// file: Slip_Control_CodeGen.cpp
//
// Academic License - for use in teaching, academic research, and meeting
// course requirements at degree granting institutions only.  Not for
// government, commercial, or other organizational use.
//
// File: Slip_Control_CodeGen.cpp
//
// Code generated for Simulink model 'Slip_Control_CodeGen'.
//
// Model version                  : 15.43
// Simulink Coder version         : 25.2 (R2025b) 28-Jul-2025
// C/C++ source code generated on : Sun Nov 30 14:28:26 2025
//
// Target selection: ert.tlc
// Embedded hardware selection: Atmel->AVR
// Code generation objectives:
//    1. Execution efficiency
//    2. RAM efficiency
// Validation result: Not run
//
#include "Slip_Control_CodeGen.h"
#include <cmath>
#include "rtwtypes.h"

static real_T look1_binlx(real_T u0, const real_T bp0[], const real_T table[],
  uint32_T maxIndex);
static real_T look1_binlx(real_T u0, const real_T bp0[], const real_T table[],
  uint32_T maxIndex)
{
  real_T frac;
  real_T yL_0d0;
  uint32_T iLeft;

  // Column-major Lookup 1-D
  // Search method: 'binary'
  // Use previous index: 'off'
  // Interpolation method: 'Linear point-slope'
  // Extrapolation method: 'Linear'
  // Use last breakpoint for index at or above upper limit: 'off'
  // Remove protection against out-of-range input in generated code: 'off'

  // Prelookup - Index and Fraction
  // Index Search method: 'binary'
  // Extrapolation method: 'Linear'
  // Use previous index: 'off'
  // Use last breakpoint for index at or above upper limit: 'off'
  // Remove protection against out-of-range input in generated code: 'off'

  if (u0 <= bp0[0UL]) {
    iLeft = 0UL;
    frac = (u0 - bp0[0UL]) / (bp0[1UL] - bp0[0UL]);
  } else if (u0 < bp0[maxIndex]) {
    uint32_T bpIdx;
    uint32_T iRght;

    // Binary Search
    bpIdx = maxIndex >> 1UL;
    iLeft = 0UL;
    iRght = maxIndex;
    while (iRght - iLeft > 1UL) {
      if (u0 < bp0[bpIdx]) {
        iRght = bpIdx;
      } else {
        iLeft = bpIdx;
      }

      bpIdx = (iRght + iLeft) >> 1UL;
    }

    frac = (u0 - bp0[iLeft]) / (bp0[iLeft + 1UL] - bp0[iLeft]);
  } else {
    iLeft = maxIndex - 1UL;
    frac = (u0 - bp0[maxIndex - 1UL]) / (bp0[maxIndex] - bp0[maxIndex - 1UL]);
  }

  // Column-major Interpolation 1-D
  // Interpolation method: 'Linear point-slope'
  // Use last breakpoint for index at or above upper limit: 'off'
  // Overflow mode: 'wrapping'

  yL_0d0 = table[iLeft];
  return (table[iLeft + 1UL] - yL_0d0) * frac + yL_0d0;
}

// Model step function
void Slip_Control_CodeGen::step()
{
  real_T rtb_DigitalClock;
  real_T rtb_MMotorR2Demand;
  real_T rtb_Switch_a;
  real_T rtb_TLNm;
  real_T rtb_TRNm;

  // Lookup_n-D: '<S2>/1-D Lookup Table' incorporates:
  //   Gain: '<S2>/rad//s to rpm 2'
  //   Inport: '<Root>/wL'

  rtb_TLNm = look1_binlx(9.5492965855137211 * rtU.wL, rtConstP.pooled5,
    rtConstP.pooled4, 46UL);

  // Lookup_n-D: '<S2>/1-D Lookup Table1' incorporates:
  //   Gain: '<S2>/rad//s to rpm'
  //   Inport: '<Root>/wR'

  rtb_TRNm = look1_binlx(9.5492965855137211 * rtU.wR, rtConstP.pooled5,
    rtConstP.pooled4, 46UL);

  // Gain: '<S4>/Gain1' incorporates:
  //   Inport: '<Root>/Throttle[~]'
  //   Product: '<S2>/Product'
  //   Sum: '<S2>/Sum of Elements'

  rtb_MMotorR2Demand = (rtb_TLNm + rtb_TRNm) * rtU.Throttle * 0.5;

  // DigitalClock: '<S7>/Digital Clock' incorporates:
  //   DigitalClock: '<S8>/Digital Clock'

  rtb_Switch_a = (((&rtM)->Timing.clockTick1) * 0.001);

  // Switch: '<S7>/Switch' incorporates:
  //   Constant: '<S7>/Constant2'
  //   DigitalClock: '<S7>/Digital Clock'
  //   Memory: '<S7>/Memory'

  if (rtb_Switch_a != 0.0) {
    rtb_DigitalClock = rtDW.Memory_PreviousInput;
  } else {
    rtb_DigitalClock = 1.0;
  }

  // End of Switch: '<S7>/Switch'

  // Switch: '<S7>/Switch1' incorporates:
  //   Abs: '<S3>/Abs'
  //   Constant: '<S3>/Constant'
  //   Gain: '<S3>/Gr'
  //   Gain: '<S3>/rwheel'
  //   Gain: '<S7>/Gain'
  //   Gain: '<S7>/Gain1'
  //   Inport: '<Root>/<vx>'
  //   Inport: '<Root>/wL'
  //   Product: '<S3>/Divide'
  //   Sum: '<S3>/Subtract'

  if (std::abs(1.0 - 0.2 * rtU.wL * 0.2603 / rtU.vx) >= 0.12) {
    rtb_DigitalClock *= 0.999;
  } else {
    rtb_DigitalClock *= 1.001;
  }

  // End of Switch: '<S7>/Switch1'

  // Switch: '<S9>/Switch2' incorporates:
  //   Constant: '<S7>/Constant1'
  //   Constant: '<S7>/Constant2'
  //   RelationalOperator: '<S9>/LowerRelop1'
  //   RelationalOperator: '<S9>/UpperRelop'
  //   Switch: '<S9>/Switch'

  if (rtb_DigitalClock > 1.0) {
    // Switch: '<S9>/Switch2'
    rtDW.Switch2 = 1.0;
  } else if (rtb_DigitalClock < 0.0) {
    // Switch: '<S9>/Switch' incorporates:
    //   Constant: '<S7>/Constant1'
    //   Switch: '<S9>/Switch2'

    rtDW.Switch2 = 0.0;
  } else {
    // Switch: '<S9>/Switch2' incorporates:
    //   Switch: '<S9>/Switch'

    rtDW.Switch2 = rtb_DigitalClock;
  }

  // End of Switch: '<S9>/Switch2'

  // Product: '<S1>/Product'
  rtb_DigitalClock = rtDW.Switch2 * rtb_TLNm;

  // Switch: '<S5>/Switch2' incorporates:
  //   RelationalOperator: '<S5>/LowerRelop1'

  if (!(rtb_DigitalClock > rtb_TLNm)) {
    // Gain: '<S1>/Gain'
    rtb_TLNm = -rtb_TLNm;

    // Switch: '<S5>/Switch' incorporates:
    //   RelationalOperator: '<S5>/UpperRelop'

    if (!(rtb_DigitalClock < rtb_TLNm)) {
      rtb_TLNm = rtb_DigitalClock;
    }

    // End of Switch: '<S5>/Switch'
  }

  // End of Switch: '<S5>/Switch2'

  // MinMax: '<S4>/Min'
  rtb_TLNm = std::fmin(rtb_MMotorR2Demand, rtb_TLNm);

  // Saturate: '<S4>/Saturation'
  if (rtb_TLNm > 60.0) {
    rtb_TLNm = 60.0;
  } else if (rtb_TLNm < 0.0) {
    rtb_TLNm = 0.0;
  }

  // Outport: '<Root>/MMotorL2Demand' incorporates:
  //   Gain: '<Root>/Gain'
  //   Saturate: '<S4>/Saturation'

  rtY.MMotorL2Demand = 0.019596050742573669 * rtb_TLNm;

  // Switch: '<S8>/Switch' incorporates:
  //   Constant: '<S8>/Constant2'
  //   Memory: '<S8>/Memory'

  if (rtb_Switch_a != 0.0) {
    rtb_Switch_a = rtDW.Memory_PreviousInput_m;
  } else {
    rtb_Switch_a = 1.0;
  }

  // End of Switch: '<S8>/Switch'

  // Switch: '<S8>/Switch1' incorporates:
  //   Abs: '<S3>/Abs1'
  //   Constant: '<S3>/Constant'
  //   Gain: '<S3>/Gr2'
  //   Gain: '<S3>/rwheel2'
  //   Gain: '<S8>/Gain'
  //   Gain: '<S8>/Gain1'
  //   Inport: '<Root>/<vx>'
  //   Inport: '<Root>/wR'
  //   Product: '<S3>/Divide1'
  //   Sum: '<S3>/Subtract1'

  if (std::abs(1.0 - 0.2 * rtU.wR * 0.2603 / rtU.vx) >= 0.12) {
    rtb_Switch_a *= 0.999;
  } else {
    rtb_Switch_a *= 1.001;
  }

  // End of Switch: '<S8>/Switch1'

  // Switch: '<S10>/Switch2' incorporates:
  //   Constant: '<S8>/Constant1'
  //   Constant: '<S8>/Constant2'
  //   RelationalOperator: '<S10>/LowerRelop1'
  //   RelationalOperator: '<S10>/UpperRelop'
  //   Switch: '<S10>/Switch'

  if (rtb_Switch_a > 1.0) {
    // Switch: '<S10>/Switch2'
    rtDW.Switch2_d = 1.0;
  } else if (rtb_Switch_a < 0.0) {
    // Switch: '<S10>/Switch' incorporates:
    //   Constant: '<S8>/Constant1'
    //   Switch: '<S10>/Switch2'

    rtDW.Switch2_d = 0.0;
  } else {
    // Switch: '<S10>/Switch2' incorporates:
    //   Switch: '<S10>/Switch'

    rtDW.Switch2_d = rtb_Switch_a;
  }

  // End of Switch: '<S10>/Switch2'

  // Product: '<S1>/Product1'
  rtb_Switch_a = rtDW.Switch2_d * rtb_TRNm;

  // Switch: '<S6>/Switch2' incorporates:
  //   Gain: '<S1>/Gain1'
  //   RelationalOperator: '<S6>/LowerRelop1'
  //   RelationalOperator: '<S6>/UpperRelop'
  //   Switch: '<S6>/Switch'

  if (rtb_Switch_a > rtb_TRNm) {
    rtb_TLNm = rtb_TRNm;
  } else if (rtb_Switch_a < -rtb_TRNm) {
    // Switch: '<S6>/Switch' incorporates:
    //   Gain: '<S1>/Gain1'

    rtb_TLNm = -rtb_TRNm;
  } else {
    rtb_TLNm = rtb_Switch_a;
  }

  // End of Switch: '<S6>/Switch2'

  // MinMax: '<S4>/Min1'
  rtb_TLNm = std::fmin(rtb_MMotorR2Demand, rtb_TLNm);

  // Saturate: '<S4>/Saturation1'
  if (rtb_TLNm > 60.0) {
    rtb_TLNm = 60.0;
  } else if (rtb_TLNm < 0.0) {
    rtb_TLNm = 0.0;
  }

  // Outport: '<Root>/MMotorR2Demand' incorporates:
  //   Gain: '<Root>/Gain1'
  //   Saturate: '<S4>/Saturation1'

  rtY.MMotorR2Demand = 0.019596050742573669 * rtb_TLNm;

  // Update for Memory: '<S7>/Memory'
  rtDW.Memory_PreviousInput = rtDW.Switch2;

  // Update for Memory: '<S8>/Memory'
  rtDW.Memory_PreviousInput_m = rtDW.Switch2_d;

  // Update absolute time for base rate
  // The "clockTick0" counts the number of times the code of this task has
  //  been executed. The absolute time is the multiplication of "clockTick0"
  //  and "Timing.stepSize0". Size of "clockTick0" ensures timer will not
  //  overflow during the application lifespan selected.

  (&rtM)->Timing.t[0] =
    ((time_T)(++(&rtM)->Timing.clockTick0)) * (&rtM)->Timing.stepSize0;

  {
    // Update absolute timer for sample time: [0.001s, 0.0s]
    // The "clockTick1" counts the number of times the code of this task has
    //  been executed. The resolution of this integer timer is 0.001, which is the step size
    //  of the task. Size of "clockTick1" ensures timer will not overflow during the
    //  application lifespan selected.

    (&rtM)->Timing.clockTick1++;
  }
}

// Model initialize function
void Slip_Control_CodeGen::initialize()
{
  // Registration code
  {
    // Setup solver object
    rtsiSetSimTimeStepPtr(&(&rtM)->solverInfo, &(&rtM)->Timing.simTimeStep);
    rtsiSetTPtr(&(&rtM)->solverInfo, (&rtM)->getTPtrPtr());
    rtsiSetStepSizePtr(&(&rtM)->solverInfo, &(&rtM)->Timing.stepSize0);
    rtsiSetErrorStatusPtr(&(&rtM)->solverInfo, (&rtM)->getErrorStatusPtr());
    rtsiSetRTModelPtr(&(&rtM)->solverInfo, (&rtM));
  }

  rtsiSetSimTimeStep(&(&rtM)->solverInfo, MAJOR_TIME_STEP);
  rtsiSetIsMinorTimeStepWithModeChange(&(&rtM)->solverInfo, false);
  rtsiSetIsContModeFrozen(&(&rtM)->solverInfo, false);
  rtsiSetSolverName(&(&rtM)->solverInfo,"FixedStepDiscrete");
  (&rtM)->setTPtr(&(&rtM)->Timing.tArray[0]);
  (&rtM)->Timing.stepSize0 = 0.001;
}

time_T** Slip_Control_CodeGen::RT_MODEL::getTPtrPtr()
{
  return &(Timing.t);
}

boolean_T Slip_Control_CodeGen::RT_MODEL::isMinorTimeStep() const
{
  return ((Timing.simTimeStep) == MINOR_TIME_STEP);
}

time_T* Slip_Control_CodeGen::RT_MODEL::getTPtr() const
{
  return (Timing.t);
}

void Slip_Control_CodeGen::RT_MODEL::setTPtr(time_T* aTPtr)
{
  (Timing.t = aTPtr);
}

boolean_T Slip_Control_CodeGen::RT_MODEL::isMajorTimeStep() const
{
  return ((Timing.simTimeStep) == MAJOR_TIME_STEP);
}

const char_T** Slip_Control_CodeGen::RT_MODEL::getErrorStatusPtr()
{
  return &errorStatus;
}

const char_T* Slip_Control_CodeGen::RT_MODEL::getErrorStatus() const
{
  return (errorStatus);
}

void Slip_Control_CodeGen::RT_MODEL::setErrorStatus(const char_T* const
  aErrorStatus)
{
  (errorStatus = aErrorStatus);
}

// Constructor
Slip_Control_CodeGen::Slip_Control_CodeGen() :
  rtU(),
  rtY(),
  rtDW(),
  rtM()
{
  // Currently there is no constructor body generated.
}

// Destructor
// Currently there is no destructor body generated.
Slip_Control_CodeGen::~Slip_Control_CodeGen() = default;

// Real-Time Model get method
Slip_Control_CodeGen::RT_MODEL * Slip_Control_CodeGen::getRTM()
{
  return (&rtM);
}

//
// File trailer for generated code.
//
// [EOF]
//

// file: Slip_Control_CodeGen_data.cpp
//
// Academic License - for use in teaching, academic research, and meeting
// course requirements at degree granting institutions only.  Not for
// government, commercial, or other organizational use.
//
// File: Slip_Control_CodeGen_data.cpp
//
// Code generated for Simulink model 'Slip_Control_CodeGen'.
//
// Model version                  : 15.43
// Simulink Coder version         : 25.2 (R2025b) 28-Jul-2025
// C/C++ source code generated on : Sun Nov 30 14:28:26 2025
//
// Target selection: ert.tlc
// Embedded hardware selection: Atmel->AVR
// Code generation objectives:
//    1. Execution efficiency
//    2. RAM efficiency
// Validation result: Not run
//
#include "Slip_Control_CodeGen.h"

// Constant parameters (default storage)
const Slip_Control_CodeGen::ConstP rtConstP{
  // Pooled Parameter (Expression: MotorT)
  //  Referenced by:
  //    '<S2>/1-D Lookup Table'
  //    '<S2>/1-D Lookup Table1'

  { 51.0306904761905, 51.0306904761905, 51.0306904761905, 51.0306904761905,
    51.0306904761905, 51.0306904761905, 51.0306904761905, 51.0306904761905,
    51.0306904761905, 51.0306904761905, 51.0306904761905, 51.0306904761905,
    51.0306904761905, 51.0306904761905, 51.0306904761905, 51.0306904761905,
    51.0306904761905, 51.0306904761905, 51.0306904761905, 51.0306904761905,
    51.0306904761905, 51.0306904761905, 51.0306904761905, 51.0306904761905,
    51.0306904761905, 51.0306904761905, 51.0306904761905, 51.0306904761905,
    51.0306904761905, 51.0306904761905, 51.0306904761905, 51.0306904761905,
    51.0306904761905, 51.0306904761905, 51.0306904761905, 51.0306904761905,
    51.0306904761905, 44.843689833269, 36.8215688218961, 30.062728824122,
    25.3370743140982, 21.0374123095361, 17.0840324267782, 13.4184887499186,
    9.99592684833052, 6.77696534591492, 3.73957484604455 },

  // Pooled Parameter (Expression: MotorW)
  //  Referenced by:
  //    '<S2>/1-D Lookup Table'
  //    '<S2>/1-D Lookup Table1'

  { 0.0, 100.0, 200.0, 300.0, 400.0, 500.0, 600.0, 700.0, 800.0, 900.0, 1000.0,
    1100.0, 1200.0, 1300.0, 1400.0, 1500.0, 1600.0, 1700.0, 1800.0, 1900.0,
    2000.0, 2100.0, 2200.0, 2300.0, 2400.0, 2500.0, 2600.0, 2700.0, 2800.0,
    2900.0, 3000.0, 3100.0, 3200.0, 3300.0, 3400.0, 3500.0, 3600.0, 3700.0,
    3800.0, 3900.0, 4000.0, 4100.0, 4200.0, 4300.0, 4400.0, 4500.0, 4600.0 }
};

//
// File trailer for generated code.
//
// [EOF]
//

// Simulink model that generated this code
simulink model "Slip_Control_CodeGen"  (R2025b)
settings: Solver=FixedStepAuto  StartTime=0.0  StopTime=100  MaxStep=0.4  RelTol=1e-3  AbsTol=1e-3
model mask{Control=Control, Gr=Control.GearRatio, Kneg=Control.Correction.Dec, Kpos=Control.Correction.Inc, MotorT=Control.MotorTrq, MotorW=Control.MotorW, Tmax=max(Control.MotorTrq), alpha_max=Control.SlipTh+0.01, rwheel=Control.WheelRad}
  mask prompts: Control "Control Parameters"; Gr "Gear Ratio"; MotorT "Motor Torque"; MotorW "Motor RPM"; Tmax "Max Torque"; alpha_max "Slip Threshold"; rwheel "Wheel Radius"
model workspace (MAT data in the model file):
  Control : object (value not decoded)
  Gr = 5
  Kneg = 0.999
  Kpos = 1.001
  MotorT = [51.0306904762 51.0306904762 51.0306904762 51.0306904762 51.0306904762 51.0306904762 51.0306904762 51.0306904762 51.0306904762 51.0306904762 51.0306904762 51.0306904762 ... (47 elements, 1x47)]
  MotorW = [0 100 200 300 400 500 600 700 800 900 1000 1100 ... (47 elements, 1x47)]
  Tmax = 51.0306904762
  alpha_max = 0.12
  rwheel = 0.2603
libraries: simulink x4

== system Slip_Control_CodeGen ==
  <vx> : Inport  OutDataTypeStr=double  PortDimensions=1  SampleTime=0
  wL : Inport  Port=2  OutDataTypeStr=double  PortDimensions=1  SampleTime=0
  wR : Inport  Port=3  OutDataTypeStr=double  PortDimensions=1  SampleTime=0
  Throttle[~] : Inport  Port=4  OutDataTypeStr=double  PortDimensions=1  SampleTime=0
  Bus Creator : BusCreator  Inputs=2
  Gain : Gain  Gain=1/Tmax
  Gain1 : Gain  Gain=1/Tmax
  Maximum Torque Allowed : Subsystem
  Required Torque : Subsystem
  Slip Control : Subsystem
  Torque Allocation : Subsystem
  MMotorL2Demand : Outport  OutDataTypeStr=double  PortDimensions=1  SampleTime=0
  MMotorR2Demand : Outport  Port=2  OutDataTypeStr=double  PortDimensions=1  SampleTime=0
  wires:
  Slip Control/1(A) -> Maximum Torque Allowed/1(A)
  Gain1/1 -> MMotorR2Demand/1
  Maximum Torque Allowed/1(Tmax) -> Torque Allocation/1(Tmax)
  Throttle[~]/1 -> Required Torque/2(rAccelPedal)  "Throttle[~]"
  Required Torque/1(Twheels) -> Maximum Torque Allowed/3(Twheels)
  Torque Allocation/1(MMotorL2Demand) -> Gain/1  "MMotorL2Demand"
  Required Torque/2(T) -> Torque Allocation/2(T)
  Slip Control/2(B) -> Maximum Torque Allowed/2(B)
  wL/1 -> Bus Creator/1  "wL"
  Bus Creator/1 -> Slip Control/2(w), Required Torque/1(w)  "w [rad/s]"
  <vx>/1 -> Slip Control/1(Vx)  "vx"
  wR/1 -> Bus Creator/2  "wR"
  Torque Allocation/2(MMotorR2Demand) -> Gain1/1  "MMotorR2Demand"
  Gain/1 -> MMotorL2Demand/1

== system Slip_Control_CodeGen/Maximum Torque Allowed ==
  A : Inport
  B : Inport  Port=2
  Twheels : Inport  Port=3
  Bus Creator : BusCreator  Inputs=2
  Bus Selector : BusSelector  OutputSignals=TL [Nm],TR [Nm]
  Gain : Gain  Gain=-1
  Gain1 : Gain  Gain=-1
  Product : Product
  Product1 : Product
  Saturation Dynamic : simulink/Discontinuities/Saturation Dynamic  OutMin=[]  OutMax=[]  OutDataTypeStr=Inherit: Same as second input  OutDataType=fixdt(1, 16)  OutScaling=2^-10  DoSatur=off
  Saturation Dynamic1 : simulink/Discontinuities/Saturation Dynamic  OutMin=[]  OutMax=[]  OutDataTypeStr=Inherit: Same as second input  OutDataType=fixdt(1, 16)  OutScaling=2^-10  DoSatur=off
  Slip Correction Left : Subsystem
  Slip Correction Right : Subsystem
  Tmax : Outport
  wires:
  Saturation Dynamic/1 -> Bus Creator/1  "TmaxL"
  Bus Selector/2 -> Product1/2, Gain1/1, Saturation Dynamic1/1  "<TR [Nm]>"
  B/1 -> Slip Correction Right/1(B)
  A/1 -> Slip Correction Left/1(A)
  Slip Correction Right/1(Kb) -> Product1/1
  Slip Correction Left/1(Ka) -> Product/1
  Product/1 -> Saturation Dynamic/2
  Gain1/1 -> Saturation Dynamic1/3
  Bus Selector/1 -> Product/2, Saturation Dynamic/1, Gain/1  "<TL [Nm]>"
  Saturation Dynamic1/1 -> Bus Creator/2  "TmaxR"
  Twheels/1 -> Bus Selector/1
  Bus Creator/1 -> Tmax/1
  Gain/1 -> Saturation Dynamic/3
  Product1/1 -> Saturation Dynamic1/2

== system Slip_Control_CodeGen/Required Torque ==
  w : Inport
  rAccelPedal : Inport  Port=2
  1-D Lookup Table : Lookup_n-D  NumberOfTableDimensions=1  BreakpointsForDimension1=MotorW  Table=MotorT  InternalRulePriority=Speed  RndMeth=Simplest
  1-D Lookup Table1 : Lookup_n-D  NumberOfTableDimensions=1  BreakpointsForDimension1=MotorW  Table=MotorT  InternalRulePriority=Speed  RndMeth=Simplest
  Bus Creator : BusCreator  Inputs=2
  Bus Selector : BusSelector  OutputSignals=wL,wR
  Product : Product
  Sum of Elements : Sum  Inputs=+
  rad/s to rpm : Gain  Gain=60/pi/2
  rad/s to rpm 2 : Gain  Gain=60/pi/2
  Twheels : Outport
  T : Outport  Port=2
  wires:
  w/1 -> Bus Selector/1
  Sum of Elements/1 -> Product/1  "Ttot [Nm]"
  1-D Lookup Table1/1 -> Bus Creator/2  "TR [Nm]"
  rAccelPedal/1 -> Product/2  "Throttle [~]"
  rad/s to rpm/1 -> 1-D Lookup Table1/1
  Bus Selector/1 -> rad/s to rpm 2/1  "<wL>"
  Product/1 -> T/1  "T [Nm]"
  Bus Selector/2 -> rad/s to rpm/1  "<wR>"
  rad/s to rpm 2/1 -> 1-D Lookup Table/1
  1-D Lookup Table/1 -> Bus Creator/1  "TL [Nm]"
  Bus Creator/1 -> Sum of Elements/1, Twheels/1

== system Slip_Control_CodeGen/Slip Control ==
  Vx : Inport
  w : Inport  Port=2
  Abs : Abs  SaturateOnIntegerOverflow=off
  Abs1 : Abs  SaturateOnIntegerOverflow=off
  Bus Selector : BusSelector  OutputSignals=wL,wR
  Constant : Constant
  Divide : Product  Inputs=*/
  Divide1 : Product  Inputs=*/
  Gr : Gain  Gain=1/Gr
  Gr2 : Gain  Gain=1/Gr
  Scope : Scope  NumInputPorts=2
  Subtract : Sum  Inputs=+-
  Subtract1 : Sum  Inputs=+-
  rwheel : Gain  Gain=rwheel
  rwheel2 : Gain  Gain=rwheel
  A : Outport
  B : Outport  Port=2
  wires:
  rwheel2/1 -> Divide1/1  "w"
  Gr2/1 -> rwheel2/1  "w"
  Gr/1 -> rwheel/1  "w"
  rwheel/1 -> Divide/1  "w"
  w/1 -> Bus Selector/1  "w"
  Vx/1 -> Divide1/2, Divide/2
  Bus Selector/1 -> Gr/1  "<wL>"
  Subtract/1 -> Abs/1
  Subtract1/1 -> Abs1/1
  Bus Selector/2 -> Gr2/1  "<wR>"
  Constant/1 -> Subtract/1, Subtract1/1
  Divide/1 -> Subtract/2
  Divide1/1 -> Subtract1/2
  Abs/1 -> A/1, Scope/1  "A[~]"
  Abs1/1 -> B/1, Scope/2  "B[~]"

== system Slip_Control_CodeGen/Torque Allocation ==
  Tmax : Inport
  T : Inport  Port=2
  Bus Selector : BusSelector  OutputSignals=TmaxL,TmaxR
  Gain1 : Gain  Gain=1/2
  Min : MinMax  Inputs=2
  Min1 : MinMax  Inputs=2
  Saturation : Saturate  UpperLimit=60  LowerLimit=0
  Saturation1 : Saturate  UpperLimit=60  LowerLimit=0
  MMotorL2Demand : Outport
  MMotorR2Demand : Outport  Port=2
  wires:
  Bus Selector/2 -> Min1/2  "<TmaxR>"
  T/1 -> Gain1/1
  Gain1/1 -> Min1/1, Min/1
  Min1/1 -> Saturation1/1
  Min/1 -> Saturation/1
  Saturation/1 -> MMotorL2Demand/1  "MMotorL2Demand"
  Saturation1/1 -> MMotorR2Demand/1  "MMotorR2Demand"
  Tmax/1 -> Bus Selector/1
  Bus Selector/1 -> Min/2  "<TmaxL>"

== system Slip_Control_CodeGen/Maximum Torque Allowed/Slip Correction Left ==
  A : Inport
  Constant1 : Constant  Value=0
  Constant2 : Constant
  Digital Clock : DigitalClock  SampleTime=0.001
  Gain : Gain  Gain=Kneg
  Gain1 : Gain  Gain=Kpos
  Memory : Memory
  Saturation Dynamic : simulink/Discontinuities/Saturation Dynamic  OutMin=[]  OutMax=[]  OutDataTypeStr=Inherit: Same as second input  OutDataType=fixdt(1, 16)  OutScaling=2^-10  DoSatur=off
  Switch : Switch  Criteria=u2 ~= 0  SaturateOnIntegerOverflow=off  InputSameDT=off
  Switch1 : Switch  Threshold=alpha_max  SaturateOnIntegerOverflow=off  InputSameDT=off
  Ka : Outport
  wires:
  Gain/1 -> Switch1/1
  Switch1/1 -> Saturation Dynamic/2
  Digital Clock/1 -> Switch/2
  Constant1/1 -> Saturation Dynamic/3
  Switch/1 -> Gain1/1, Gain/1
  Gain1/1 -> Switch1/3
  Saturation Dynamic/1 -> Ka/1, Memory/1
  A/1 -> Switch1/2
  Constant2/1 -> Saturation Dynamic/1, Switch/3
  Memory/1 -> Switch/1

== system Slip_Control_CodeGen/Maximum Torque Allowed/Slip Correction Right ==
  B : Inport
  Constant1 : Constant  Value=0
  Constant2 : Constant
  Digital Clock : DigitalClock  SampleTime=0.001
  Gain : Gain  Gain=Kneg
  Gain1 : Gain  Gain=Kpos
  Memory : Memory
  Saturation Dynamic : simulink/Discontinuities/Saturation Dynamic  OutMin=[]  OutMax=[]  OutDataTypeStr=Inherit: Same as second input  OutDataType=fixdt(1, 16)  OutScaling=2^-10  DoSatur=off
  Switch : Switch  Criteria=u2 ~= 0  SaturateOnIntegerOverflow=off  InputSameDT=off
  Switch1 : Switch  Threshold=alpha_max  SaturateOnIntegerOverflow=off  InputSameDT=off
  Kb : Outport
  wires:
  Memory/1 -> Switch/1
  Constant2/1 -> Switch/3, Saturation Dynamic/1
  B/1 -> Switch1/2
  Saturation Dynamic/1 -> Kb/1, Memory/1
  Gain1/1 -> Switch1/3
  Switch/1 -> Gain/1, Gain1/1
  Constant1/1 -> Saturation Dynamic/3
  Digital Clock/1 -> Switch/2
  Switch1/1 -> Saturation Dynamic/2
  Gain/1 -> Switch1/1
